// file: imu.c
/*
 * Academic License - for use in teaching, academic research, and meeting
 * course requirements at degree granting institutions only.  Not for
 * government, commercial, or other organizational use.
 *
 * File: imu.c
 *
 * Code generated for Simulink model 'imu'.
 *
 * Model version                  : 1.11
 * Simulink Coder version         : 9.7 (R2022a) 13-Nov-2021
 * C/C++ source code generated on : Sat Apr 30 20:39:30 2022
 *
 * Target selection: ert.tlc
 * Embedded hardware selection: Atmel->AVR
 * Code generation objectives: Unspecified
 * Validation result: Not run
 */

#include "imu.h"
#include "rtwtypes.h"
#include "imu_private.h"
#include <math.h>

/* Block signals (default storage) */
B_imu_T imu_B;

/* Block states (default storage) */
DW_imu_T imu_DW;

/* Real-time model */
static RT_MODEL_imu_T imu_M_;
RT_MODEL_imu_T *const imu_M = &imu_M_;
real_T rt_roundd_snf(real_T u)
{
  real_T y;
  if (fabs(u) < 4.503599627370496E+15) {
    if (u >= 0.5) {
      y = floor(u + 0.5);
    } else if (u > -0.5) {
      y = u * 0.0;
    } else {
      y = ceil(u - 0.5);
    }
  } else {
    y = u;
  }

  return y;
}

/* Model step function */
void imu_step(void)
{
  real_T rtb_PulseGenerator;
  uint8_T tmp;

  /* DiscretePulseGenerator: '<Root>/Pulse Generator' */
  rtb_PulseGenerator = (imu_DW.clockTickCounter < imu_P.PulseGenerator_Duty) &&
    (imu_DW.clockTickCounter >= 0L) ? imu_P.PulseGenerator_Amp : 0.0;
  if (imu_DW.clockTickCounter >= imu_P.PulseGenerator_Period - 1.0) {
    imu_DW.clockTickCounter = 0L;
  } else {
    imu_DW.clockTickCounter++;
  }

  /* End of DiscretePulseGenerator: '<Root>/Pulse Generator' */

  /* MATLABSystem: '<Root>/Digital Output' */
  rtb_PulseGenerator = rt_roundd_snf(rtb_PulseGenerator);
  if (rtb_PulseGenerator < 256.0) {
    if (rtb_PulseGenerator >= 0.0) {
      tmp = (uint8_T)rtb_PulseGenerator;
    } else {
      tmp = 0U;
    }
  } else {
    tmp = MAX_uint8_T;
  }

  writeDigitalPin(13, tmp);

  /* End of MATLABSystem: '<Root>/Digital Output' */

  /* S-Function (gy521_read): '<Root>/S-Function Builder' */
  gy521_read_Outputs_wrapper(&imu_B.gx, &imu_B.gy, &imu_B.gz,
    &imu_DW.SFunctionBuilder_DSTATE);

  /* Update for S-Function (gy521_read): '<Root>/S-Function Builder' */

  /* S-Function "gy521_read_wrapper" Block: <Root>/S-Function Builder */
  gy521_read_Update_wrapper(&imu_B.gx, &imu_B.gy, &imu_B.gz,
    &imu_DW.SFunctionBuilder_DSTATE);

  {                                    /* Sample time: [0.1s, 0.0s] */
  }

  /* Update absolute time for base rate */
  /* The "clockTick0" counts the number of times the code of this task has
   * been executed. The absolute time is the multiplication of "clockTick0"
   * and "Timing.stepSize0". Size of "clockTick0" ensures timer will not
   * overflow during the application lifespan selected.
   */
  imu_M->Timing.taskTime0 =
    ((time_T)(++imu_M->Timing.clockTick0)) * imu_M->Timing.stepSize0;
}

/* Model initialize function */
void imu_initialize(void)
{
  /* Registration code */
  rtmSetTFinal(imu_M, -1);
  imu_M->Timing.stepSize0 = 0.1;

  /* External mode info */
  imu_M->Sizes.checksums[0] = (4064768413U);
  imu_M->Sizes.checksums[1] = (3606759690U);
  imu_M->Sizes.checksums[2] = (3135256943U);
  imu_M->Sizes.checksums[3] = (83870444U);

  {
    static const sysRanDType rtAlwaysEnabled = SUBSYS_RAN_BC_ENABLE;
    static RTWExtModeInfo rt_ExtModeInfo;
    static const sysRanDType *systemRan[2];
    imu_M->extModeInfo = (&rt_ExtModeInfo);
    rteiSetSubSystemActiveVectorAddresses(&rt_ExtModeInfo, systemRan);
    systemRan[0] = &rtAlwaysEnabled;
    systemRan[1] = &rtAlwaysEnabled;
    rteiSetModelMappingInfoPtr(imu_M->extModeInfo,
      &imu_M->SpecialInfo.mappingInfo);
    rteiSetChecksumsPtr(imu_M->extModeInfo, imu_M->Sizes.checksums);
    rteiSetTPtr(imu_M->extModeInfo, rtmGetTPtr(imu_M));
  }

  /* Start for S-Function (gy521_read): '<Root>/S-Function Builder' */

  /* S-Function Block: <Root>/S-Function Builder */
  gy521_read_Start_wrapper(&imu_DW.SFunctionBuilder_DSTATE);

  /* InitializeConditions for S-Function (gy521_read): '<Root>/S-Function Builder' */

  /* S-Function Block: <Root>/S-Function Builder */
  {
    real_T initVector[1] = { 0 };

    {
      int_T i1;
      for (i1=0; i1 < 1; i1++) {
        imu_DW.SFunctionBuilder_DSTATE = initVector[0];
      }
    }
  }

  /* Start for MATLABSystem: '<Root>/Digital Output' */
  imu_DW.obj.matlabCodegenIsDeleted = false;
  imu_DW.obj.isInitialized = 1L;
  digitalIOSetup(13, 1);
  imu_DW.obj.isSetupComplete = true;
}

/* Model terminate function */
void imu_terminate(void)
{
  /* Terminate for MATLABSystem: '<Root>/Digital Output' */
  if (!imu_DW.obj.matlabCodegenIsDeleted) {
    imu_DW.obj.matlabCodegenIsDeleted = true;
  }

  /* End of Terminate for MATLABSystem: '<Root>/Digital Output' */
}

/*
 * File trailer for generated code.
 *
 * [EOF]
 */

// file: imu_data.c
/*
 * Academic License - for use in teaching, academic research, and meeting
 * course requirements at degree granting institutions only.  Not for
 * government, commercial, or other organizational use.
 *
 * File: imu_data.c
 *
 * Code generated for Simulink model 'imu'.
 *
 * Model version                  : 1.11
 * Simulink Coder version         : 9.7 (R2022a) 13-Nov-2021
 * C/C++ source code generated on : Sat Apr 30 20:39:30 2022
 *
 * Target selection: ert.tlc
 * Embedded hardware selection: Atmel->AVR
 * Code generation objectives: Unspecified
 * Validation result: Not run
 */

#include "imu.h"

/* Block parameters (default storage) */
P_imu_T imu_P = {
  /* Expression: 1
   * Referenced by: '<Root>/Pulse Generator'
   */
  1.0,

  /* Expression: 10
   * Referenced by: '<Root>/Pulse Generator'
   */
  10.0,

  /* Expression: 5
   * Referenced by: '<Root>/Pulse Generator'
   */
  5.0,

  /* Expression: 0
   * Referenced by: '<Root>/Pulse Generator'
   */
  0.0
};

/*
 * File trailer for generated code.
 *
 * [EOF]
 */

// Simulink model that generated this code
simulink model "imu"  (R2022a)
settings: Solver=FixedStepAuto  StartTime=0.0  StopTime=inf  RelTol=1e-3  EnableMultiTasking=on
libraries: arduinolib x1

== system imu ==
  Digital Output : arduinolib/Digital Output  pinNumber=13  Direction=output  blockPlatform=arduino
  Display : Display
  Display1 : Display
  Display2 : Display
  Pulse Generator : DiscretePulseGenerator  Period=10  PulseWidth=5  SampleTime=0.1
  S-Function Builder : S-Function  FunctionName=gy521_read  SFunctionModules=gy521_read_wrapper  SFunctionDeploymentMode=off  EnableBusSupport=off  mask(S-Function Builder){}
      mask help: Simulink:masks:SFunctionBuilder_MD
      mask init:
      | val = [[.9  0.75 0.75 1 1 .9 .9 1]',[1 1 0.75 0.75 .9 .9 1 .9]'];try , sys = get_param(gcb,'SfunBuilderFcnName');if isempty(sys), sys = get_param(gcb,'FunctionName'); end,catch, sys = get_param(gcb,'FunctionName'); end
  wires:
  Pulse Generator/1 -> Digital Output/1
  S-Function Builder/1 -> Display/1  "gx"
  S-Function Builder/3 -> Display2/1  "gz"
  S-Function Builder/2 -> Display1/1  "gy"
